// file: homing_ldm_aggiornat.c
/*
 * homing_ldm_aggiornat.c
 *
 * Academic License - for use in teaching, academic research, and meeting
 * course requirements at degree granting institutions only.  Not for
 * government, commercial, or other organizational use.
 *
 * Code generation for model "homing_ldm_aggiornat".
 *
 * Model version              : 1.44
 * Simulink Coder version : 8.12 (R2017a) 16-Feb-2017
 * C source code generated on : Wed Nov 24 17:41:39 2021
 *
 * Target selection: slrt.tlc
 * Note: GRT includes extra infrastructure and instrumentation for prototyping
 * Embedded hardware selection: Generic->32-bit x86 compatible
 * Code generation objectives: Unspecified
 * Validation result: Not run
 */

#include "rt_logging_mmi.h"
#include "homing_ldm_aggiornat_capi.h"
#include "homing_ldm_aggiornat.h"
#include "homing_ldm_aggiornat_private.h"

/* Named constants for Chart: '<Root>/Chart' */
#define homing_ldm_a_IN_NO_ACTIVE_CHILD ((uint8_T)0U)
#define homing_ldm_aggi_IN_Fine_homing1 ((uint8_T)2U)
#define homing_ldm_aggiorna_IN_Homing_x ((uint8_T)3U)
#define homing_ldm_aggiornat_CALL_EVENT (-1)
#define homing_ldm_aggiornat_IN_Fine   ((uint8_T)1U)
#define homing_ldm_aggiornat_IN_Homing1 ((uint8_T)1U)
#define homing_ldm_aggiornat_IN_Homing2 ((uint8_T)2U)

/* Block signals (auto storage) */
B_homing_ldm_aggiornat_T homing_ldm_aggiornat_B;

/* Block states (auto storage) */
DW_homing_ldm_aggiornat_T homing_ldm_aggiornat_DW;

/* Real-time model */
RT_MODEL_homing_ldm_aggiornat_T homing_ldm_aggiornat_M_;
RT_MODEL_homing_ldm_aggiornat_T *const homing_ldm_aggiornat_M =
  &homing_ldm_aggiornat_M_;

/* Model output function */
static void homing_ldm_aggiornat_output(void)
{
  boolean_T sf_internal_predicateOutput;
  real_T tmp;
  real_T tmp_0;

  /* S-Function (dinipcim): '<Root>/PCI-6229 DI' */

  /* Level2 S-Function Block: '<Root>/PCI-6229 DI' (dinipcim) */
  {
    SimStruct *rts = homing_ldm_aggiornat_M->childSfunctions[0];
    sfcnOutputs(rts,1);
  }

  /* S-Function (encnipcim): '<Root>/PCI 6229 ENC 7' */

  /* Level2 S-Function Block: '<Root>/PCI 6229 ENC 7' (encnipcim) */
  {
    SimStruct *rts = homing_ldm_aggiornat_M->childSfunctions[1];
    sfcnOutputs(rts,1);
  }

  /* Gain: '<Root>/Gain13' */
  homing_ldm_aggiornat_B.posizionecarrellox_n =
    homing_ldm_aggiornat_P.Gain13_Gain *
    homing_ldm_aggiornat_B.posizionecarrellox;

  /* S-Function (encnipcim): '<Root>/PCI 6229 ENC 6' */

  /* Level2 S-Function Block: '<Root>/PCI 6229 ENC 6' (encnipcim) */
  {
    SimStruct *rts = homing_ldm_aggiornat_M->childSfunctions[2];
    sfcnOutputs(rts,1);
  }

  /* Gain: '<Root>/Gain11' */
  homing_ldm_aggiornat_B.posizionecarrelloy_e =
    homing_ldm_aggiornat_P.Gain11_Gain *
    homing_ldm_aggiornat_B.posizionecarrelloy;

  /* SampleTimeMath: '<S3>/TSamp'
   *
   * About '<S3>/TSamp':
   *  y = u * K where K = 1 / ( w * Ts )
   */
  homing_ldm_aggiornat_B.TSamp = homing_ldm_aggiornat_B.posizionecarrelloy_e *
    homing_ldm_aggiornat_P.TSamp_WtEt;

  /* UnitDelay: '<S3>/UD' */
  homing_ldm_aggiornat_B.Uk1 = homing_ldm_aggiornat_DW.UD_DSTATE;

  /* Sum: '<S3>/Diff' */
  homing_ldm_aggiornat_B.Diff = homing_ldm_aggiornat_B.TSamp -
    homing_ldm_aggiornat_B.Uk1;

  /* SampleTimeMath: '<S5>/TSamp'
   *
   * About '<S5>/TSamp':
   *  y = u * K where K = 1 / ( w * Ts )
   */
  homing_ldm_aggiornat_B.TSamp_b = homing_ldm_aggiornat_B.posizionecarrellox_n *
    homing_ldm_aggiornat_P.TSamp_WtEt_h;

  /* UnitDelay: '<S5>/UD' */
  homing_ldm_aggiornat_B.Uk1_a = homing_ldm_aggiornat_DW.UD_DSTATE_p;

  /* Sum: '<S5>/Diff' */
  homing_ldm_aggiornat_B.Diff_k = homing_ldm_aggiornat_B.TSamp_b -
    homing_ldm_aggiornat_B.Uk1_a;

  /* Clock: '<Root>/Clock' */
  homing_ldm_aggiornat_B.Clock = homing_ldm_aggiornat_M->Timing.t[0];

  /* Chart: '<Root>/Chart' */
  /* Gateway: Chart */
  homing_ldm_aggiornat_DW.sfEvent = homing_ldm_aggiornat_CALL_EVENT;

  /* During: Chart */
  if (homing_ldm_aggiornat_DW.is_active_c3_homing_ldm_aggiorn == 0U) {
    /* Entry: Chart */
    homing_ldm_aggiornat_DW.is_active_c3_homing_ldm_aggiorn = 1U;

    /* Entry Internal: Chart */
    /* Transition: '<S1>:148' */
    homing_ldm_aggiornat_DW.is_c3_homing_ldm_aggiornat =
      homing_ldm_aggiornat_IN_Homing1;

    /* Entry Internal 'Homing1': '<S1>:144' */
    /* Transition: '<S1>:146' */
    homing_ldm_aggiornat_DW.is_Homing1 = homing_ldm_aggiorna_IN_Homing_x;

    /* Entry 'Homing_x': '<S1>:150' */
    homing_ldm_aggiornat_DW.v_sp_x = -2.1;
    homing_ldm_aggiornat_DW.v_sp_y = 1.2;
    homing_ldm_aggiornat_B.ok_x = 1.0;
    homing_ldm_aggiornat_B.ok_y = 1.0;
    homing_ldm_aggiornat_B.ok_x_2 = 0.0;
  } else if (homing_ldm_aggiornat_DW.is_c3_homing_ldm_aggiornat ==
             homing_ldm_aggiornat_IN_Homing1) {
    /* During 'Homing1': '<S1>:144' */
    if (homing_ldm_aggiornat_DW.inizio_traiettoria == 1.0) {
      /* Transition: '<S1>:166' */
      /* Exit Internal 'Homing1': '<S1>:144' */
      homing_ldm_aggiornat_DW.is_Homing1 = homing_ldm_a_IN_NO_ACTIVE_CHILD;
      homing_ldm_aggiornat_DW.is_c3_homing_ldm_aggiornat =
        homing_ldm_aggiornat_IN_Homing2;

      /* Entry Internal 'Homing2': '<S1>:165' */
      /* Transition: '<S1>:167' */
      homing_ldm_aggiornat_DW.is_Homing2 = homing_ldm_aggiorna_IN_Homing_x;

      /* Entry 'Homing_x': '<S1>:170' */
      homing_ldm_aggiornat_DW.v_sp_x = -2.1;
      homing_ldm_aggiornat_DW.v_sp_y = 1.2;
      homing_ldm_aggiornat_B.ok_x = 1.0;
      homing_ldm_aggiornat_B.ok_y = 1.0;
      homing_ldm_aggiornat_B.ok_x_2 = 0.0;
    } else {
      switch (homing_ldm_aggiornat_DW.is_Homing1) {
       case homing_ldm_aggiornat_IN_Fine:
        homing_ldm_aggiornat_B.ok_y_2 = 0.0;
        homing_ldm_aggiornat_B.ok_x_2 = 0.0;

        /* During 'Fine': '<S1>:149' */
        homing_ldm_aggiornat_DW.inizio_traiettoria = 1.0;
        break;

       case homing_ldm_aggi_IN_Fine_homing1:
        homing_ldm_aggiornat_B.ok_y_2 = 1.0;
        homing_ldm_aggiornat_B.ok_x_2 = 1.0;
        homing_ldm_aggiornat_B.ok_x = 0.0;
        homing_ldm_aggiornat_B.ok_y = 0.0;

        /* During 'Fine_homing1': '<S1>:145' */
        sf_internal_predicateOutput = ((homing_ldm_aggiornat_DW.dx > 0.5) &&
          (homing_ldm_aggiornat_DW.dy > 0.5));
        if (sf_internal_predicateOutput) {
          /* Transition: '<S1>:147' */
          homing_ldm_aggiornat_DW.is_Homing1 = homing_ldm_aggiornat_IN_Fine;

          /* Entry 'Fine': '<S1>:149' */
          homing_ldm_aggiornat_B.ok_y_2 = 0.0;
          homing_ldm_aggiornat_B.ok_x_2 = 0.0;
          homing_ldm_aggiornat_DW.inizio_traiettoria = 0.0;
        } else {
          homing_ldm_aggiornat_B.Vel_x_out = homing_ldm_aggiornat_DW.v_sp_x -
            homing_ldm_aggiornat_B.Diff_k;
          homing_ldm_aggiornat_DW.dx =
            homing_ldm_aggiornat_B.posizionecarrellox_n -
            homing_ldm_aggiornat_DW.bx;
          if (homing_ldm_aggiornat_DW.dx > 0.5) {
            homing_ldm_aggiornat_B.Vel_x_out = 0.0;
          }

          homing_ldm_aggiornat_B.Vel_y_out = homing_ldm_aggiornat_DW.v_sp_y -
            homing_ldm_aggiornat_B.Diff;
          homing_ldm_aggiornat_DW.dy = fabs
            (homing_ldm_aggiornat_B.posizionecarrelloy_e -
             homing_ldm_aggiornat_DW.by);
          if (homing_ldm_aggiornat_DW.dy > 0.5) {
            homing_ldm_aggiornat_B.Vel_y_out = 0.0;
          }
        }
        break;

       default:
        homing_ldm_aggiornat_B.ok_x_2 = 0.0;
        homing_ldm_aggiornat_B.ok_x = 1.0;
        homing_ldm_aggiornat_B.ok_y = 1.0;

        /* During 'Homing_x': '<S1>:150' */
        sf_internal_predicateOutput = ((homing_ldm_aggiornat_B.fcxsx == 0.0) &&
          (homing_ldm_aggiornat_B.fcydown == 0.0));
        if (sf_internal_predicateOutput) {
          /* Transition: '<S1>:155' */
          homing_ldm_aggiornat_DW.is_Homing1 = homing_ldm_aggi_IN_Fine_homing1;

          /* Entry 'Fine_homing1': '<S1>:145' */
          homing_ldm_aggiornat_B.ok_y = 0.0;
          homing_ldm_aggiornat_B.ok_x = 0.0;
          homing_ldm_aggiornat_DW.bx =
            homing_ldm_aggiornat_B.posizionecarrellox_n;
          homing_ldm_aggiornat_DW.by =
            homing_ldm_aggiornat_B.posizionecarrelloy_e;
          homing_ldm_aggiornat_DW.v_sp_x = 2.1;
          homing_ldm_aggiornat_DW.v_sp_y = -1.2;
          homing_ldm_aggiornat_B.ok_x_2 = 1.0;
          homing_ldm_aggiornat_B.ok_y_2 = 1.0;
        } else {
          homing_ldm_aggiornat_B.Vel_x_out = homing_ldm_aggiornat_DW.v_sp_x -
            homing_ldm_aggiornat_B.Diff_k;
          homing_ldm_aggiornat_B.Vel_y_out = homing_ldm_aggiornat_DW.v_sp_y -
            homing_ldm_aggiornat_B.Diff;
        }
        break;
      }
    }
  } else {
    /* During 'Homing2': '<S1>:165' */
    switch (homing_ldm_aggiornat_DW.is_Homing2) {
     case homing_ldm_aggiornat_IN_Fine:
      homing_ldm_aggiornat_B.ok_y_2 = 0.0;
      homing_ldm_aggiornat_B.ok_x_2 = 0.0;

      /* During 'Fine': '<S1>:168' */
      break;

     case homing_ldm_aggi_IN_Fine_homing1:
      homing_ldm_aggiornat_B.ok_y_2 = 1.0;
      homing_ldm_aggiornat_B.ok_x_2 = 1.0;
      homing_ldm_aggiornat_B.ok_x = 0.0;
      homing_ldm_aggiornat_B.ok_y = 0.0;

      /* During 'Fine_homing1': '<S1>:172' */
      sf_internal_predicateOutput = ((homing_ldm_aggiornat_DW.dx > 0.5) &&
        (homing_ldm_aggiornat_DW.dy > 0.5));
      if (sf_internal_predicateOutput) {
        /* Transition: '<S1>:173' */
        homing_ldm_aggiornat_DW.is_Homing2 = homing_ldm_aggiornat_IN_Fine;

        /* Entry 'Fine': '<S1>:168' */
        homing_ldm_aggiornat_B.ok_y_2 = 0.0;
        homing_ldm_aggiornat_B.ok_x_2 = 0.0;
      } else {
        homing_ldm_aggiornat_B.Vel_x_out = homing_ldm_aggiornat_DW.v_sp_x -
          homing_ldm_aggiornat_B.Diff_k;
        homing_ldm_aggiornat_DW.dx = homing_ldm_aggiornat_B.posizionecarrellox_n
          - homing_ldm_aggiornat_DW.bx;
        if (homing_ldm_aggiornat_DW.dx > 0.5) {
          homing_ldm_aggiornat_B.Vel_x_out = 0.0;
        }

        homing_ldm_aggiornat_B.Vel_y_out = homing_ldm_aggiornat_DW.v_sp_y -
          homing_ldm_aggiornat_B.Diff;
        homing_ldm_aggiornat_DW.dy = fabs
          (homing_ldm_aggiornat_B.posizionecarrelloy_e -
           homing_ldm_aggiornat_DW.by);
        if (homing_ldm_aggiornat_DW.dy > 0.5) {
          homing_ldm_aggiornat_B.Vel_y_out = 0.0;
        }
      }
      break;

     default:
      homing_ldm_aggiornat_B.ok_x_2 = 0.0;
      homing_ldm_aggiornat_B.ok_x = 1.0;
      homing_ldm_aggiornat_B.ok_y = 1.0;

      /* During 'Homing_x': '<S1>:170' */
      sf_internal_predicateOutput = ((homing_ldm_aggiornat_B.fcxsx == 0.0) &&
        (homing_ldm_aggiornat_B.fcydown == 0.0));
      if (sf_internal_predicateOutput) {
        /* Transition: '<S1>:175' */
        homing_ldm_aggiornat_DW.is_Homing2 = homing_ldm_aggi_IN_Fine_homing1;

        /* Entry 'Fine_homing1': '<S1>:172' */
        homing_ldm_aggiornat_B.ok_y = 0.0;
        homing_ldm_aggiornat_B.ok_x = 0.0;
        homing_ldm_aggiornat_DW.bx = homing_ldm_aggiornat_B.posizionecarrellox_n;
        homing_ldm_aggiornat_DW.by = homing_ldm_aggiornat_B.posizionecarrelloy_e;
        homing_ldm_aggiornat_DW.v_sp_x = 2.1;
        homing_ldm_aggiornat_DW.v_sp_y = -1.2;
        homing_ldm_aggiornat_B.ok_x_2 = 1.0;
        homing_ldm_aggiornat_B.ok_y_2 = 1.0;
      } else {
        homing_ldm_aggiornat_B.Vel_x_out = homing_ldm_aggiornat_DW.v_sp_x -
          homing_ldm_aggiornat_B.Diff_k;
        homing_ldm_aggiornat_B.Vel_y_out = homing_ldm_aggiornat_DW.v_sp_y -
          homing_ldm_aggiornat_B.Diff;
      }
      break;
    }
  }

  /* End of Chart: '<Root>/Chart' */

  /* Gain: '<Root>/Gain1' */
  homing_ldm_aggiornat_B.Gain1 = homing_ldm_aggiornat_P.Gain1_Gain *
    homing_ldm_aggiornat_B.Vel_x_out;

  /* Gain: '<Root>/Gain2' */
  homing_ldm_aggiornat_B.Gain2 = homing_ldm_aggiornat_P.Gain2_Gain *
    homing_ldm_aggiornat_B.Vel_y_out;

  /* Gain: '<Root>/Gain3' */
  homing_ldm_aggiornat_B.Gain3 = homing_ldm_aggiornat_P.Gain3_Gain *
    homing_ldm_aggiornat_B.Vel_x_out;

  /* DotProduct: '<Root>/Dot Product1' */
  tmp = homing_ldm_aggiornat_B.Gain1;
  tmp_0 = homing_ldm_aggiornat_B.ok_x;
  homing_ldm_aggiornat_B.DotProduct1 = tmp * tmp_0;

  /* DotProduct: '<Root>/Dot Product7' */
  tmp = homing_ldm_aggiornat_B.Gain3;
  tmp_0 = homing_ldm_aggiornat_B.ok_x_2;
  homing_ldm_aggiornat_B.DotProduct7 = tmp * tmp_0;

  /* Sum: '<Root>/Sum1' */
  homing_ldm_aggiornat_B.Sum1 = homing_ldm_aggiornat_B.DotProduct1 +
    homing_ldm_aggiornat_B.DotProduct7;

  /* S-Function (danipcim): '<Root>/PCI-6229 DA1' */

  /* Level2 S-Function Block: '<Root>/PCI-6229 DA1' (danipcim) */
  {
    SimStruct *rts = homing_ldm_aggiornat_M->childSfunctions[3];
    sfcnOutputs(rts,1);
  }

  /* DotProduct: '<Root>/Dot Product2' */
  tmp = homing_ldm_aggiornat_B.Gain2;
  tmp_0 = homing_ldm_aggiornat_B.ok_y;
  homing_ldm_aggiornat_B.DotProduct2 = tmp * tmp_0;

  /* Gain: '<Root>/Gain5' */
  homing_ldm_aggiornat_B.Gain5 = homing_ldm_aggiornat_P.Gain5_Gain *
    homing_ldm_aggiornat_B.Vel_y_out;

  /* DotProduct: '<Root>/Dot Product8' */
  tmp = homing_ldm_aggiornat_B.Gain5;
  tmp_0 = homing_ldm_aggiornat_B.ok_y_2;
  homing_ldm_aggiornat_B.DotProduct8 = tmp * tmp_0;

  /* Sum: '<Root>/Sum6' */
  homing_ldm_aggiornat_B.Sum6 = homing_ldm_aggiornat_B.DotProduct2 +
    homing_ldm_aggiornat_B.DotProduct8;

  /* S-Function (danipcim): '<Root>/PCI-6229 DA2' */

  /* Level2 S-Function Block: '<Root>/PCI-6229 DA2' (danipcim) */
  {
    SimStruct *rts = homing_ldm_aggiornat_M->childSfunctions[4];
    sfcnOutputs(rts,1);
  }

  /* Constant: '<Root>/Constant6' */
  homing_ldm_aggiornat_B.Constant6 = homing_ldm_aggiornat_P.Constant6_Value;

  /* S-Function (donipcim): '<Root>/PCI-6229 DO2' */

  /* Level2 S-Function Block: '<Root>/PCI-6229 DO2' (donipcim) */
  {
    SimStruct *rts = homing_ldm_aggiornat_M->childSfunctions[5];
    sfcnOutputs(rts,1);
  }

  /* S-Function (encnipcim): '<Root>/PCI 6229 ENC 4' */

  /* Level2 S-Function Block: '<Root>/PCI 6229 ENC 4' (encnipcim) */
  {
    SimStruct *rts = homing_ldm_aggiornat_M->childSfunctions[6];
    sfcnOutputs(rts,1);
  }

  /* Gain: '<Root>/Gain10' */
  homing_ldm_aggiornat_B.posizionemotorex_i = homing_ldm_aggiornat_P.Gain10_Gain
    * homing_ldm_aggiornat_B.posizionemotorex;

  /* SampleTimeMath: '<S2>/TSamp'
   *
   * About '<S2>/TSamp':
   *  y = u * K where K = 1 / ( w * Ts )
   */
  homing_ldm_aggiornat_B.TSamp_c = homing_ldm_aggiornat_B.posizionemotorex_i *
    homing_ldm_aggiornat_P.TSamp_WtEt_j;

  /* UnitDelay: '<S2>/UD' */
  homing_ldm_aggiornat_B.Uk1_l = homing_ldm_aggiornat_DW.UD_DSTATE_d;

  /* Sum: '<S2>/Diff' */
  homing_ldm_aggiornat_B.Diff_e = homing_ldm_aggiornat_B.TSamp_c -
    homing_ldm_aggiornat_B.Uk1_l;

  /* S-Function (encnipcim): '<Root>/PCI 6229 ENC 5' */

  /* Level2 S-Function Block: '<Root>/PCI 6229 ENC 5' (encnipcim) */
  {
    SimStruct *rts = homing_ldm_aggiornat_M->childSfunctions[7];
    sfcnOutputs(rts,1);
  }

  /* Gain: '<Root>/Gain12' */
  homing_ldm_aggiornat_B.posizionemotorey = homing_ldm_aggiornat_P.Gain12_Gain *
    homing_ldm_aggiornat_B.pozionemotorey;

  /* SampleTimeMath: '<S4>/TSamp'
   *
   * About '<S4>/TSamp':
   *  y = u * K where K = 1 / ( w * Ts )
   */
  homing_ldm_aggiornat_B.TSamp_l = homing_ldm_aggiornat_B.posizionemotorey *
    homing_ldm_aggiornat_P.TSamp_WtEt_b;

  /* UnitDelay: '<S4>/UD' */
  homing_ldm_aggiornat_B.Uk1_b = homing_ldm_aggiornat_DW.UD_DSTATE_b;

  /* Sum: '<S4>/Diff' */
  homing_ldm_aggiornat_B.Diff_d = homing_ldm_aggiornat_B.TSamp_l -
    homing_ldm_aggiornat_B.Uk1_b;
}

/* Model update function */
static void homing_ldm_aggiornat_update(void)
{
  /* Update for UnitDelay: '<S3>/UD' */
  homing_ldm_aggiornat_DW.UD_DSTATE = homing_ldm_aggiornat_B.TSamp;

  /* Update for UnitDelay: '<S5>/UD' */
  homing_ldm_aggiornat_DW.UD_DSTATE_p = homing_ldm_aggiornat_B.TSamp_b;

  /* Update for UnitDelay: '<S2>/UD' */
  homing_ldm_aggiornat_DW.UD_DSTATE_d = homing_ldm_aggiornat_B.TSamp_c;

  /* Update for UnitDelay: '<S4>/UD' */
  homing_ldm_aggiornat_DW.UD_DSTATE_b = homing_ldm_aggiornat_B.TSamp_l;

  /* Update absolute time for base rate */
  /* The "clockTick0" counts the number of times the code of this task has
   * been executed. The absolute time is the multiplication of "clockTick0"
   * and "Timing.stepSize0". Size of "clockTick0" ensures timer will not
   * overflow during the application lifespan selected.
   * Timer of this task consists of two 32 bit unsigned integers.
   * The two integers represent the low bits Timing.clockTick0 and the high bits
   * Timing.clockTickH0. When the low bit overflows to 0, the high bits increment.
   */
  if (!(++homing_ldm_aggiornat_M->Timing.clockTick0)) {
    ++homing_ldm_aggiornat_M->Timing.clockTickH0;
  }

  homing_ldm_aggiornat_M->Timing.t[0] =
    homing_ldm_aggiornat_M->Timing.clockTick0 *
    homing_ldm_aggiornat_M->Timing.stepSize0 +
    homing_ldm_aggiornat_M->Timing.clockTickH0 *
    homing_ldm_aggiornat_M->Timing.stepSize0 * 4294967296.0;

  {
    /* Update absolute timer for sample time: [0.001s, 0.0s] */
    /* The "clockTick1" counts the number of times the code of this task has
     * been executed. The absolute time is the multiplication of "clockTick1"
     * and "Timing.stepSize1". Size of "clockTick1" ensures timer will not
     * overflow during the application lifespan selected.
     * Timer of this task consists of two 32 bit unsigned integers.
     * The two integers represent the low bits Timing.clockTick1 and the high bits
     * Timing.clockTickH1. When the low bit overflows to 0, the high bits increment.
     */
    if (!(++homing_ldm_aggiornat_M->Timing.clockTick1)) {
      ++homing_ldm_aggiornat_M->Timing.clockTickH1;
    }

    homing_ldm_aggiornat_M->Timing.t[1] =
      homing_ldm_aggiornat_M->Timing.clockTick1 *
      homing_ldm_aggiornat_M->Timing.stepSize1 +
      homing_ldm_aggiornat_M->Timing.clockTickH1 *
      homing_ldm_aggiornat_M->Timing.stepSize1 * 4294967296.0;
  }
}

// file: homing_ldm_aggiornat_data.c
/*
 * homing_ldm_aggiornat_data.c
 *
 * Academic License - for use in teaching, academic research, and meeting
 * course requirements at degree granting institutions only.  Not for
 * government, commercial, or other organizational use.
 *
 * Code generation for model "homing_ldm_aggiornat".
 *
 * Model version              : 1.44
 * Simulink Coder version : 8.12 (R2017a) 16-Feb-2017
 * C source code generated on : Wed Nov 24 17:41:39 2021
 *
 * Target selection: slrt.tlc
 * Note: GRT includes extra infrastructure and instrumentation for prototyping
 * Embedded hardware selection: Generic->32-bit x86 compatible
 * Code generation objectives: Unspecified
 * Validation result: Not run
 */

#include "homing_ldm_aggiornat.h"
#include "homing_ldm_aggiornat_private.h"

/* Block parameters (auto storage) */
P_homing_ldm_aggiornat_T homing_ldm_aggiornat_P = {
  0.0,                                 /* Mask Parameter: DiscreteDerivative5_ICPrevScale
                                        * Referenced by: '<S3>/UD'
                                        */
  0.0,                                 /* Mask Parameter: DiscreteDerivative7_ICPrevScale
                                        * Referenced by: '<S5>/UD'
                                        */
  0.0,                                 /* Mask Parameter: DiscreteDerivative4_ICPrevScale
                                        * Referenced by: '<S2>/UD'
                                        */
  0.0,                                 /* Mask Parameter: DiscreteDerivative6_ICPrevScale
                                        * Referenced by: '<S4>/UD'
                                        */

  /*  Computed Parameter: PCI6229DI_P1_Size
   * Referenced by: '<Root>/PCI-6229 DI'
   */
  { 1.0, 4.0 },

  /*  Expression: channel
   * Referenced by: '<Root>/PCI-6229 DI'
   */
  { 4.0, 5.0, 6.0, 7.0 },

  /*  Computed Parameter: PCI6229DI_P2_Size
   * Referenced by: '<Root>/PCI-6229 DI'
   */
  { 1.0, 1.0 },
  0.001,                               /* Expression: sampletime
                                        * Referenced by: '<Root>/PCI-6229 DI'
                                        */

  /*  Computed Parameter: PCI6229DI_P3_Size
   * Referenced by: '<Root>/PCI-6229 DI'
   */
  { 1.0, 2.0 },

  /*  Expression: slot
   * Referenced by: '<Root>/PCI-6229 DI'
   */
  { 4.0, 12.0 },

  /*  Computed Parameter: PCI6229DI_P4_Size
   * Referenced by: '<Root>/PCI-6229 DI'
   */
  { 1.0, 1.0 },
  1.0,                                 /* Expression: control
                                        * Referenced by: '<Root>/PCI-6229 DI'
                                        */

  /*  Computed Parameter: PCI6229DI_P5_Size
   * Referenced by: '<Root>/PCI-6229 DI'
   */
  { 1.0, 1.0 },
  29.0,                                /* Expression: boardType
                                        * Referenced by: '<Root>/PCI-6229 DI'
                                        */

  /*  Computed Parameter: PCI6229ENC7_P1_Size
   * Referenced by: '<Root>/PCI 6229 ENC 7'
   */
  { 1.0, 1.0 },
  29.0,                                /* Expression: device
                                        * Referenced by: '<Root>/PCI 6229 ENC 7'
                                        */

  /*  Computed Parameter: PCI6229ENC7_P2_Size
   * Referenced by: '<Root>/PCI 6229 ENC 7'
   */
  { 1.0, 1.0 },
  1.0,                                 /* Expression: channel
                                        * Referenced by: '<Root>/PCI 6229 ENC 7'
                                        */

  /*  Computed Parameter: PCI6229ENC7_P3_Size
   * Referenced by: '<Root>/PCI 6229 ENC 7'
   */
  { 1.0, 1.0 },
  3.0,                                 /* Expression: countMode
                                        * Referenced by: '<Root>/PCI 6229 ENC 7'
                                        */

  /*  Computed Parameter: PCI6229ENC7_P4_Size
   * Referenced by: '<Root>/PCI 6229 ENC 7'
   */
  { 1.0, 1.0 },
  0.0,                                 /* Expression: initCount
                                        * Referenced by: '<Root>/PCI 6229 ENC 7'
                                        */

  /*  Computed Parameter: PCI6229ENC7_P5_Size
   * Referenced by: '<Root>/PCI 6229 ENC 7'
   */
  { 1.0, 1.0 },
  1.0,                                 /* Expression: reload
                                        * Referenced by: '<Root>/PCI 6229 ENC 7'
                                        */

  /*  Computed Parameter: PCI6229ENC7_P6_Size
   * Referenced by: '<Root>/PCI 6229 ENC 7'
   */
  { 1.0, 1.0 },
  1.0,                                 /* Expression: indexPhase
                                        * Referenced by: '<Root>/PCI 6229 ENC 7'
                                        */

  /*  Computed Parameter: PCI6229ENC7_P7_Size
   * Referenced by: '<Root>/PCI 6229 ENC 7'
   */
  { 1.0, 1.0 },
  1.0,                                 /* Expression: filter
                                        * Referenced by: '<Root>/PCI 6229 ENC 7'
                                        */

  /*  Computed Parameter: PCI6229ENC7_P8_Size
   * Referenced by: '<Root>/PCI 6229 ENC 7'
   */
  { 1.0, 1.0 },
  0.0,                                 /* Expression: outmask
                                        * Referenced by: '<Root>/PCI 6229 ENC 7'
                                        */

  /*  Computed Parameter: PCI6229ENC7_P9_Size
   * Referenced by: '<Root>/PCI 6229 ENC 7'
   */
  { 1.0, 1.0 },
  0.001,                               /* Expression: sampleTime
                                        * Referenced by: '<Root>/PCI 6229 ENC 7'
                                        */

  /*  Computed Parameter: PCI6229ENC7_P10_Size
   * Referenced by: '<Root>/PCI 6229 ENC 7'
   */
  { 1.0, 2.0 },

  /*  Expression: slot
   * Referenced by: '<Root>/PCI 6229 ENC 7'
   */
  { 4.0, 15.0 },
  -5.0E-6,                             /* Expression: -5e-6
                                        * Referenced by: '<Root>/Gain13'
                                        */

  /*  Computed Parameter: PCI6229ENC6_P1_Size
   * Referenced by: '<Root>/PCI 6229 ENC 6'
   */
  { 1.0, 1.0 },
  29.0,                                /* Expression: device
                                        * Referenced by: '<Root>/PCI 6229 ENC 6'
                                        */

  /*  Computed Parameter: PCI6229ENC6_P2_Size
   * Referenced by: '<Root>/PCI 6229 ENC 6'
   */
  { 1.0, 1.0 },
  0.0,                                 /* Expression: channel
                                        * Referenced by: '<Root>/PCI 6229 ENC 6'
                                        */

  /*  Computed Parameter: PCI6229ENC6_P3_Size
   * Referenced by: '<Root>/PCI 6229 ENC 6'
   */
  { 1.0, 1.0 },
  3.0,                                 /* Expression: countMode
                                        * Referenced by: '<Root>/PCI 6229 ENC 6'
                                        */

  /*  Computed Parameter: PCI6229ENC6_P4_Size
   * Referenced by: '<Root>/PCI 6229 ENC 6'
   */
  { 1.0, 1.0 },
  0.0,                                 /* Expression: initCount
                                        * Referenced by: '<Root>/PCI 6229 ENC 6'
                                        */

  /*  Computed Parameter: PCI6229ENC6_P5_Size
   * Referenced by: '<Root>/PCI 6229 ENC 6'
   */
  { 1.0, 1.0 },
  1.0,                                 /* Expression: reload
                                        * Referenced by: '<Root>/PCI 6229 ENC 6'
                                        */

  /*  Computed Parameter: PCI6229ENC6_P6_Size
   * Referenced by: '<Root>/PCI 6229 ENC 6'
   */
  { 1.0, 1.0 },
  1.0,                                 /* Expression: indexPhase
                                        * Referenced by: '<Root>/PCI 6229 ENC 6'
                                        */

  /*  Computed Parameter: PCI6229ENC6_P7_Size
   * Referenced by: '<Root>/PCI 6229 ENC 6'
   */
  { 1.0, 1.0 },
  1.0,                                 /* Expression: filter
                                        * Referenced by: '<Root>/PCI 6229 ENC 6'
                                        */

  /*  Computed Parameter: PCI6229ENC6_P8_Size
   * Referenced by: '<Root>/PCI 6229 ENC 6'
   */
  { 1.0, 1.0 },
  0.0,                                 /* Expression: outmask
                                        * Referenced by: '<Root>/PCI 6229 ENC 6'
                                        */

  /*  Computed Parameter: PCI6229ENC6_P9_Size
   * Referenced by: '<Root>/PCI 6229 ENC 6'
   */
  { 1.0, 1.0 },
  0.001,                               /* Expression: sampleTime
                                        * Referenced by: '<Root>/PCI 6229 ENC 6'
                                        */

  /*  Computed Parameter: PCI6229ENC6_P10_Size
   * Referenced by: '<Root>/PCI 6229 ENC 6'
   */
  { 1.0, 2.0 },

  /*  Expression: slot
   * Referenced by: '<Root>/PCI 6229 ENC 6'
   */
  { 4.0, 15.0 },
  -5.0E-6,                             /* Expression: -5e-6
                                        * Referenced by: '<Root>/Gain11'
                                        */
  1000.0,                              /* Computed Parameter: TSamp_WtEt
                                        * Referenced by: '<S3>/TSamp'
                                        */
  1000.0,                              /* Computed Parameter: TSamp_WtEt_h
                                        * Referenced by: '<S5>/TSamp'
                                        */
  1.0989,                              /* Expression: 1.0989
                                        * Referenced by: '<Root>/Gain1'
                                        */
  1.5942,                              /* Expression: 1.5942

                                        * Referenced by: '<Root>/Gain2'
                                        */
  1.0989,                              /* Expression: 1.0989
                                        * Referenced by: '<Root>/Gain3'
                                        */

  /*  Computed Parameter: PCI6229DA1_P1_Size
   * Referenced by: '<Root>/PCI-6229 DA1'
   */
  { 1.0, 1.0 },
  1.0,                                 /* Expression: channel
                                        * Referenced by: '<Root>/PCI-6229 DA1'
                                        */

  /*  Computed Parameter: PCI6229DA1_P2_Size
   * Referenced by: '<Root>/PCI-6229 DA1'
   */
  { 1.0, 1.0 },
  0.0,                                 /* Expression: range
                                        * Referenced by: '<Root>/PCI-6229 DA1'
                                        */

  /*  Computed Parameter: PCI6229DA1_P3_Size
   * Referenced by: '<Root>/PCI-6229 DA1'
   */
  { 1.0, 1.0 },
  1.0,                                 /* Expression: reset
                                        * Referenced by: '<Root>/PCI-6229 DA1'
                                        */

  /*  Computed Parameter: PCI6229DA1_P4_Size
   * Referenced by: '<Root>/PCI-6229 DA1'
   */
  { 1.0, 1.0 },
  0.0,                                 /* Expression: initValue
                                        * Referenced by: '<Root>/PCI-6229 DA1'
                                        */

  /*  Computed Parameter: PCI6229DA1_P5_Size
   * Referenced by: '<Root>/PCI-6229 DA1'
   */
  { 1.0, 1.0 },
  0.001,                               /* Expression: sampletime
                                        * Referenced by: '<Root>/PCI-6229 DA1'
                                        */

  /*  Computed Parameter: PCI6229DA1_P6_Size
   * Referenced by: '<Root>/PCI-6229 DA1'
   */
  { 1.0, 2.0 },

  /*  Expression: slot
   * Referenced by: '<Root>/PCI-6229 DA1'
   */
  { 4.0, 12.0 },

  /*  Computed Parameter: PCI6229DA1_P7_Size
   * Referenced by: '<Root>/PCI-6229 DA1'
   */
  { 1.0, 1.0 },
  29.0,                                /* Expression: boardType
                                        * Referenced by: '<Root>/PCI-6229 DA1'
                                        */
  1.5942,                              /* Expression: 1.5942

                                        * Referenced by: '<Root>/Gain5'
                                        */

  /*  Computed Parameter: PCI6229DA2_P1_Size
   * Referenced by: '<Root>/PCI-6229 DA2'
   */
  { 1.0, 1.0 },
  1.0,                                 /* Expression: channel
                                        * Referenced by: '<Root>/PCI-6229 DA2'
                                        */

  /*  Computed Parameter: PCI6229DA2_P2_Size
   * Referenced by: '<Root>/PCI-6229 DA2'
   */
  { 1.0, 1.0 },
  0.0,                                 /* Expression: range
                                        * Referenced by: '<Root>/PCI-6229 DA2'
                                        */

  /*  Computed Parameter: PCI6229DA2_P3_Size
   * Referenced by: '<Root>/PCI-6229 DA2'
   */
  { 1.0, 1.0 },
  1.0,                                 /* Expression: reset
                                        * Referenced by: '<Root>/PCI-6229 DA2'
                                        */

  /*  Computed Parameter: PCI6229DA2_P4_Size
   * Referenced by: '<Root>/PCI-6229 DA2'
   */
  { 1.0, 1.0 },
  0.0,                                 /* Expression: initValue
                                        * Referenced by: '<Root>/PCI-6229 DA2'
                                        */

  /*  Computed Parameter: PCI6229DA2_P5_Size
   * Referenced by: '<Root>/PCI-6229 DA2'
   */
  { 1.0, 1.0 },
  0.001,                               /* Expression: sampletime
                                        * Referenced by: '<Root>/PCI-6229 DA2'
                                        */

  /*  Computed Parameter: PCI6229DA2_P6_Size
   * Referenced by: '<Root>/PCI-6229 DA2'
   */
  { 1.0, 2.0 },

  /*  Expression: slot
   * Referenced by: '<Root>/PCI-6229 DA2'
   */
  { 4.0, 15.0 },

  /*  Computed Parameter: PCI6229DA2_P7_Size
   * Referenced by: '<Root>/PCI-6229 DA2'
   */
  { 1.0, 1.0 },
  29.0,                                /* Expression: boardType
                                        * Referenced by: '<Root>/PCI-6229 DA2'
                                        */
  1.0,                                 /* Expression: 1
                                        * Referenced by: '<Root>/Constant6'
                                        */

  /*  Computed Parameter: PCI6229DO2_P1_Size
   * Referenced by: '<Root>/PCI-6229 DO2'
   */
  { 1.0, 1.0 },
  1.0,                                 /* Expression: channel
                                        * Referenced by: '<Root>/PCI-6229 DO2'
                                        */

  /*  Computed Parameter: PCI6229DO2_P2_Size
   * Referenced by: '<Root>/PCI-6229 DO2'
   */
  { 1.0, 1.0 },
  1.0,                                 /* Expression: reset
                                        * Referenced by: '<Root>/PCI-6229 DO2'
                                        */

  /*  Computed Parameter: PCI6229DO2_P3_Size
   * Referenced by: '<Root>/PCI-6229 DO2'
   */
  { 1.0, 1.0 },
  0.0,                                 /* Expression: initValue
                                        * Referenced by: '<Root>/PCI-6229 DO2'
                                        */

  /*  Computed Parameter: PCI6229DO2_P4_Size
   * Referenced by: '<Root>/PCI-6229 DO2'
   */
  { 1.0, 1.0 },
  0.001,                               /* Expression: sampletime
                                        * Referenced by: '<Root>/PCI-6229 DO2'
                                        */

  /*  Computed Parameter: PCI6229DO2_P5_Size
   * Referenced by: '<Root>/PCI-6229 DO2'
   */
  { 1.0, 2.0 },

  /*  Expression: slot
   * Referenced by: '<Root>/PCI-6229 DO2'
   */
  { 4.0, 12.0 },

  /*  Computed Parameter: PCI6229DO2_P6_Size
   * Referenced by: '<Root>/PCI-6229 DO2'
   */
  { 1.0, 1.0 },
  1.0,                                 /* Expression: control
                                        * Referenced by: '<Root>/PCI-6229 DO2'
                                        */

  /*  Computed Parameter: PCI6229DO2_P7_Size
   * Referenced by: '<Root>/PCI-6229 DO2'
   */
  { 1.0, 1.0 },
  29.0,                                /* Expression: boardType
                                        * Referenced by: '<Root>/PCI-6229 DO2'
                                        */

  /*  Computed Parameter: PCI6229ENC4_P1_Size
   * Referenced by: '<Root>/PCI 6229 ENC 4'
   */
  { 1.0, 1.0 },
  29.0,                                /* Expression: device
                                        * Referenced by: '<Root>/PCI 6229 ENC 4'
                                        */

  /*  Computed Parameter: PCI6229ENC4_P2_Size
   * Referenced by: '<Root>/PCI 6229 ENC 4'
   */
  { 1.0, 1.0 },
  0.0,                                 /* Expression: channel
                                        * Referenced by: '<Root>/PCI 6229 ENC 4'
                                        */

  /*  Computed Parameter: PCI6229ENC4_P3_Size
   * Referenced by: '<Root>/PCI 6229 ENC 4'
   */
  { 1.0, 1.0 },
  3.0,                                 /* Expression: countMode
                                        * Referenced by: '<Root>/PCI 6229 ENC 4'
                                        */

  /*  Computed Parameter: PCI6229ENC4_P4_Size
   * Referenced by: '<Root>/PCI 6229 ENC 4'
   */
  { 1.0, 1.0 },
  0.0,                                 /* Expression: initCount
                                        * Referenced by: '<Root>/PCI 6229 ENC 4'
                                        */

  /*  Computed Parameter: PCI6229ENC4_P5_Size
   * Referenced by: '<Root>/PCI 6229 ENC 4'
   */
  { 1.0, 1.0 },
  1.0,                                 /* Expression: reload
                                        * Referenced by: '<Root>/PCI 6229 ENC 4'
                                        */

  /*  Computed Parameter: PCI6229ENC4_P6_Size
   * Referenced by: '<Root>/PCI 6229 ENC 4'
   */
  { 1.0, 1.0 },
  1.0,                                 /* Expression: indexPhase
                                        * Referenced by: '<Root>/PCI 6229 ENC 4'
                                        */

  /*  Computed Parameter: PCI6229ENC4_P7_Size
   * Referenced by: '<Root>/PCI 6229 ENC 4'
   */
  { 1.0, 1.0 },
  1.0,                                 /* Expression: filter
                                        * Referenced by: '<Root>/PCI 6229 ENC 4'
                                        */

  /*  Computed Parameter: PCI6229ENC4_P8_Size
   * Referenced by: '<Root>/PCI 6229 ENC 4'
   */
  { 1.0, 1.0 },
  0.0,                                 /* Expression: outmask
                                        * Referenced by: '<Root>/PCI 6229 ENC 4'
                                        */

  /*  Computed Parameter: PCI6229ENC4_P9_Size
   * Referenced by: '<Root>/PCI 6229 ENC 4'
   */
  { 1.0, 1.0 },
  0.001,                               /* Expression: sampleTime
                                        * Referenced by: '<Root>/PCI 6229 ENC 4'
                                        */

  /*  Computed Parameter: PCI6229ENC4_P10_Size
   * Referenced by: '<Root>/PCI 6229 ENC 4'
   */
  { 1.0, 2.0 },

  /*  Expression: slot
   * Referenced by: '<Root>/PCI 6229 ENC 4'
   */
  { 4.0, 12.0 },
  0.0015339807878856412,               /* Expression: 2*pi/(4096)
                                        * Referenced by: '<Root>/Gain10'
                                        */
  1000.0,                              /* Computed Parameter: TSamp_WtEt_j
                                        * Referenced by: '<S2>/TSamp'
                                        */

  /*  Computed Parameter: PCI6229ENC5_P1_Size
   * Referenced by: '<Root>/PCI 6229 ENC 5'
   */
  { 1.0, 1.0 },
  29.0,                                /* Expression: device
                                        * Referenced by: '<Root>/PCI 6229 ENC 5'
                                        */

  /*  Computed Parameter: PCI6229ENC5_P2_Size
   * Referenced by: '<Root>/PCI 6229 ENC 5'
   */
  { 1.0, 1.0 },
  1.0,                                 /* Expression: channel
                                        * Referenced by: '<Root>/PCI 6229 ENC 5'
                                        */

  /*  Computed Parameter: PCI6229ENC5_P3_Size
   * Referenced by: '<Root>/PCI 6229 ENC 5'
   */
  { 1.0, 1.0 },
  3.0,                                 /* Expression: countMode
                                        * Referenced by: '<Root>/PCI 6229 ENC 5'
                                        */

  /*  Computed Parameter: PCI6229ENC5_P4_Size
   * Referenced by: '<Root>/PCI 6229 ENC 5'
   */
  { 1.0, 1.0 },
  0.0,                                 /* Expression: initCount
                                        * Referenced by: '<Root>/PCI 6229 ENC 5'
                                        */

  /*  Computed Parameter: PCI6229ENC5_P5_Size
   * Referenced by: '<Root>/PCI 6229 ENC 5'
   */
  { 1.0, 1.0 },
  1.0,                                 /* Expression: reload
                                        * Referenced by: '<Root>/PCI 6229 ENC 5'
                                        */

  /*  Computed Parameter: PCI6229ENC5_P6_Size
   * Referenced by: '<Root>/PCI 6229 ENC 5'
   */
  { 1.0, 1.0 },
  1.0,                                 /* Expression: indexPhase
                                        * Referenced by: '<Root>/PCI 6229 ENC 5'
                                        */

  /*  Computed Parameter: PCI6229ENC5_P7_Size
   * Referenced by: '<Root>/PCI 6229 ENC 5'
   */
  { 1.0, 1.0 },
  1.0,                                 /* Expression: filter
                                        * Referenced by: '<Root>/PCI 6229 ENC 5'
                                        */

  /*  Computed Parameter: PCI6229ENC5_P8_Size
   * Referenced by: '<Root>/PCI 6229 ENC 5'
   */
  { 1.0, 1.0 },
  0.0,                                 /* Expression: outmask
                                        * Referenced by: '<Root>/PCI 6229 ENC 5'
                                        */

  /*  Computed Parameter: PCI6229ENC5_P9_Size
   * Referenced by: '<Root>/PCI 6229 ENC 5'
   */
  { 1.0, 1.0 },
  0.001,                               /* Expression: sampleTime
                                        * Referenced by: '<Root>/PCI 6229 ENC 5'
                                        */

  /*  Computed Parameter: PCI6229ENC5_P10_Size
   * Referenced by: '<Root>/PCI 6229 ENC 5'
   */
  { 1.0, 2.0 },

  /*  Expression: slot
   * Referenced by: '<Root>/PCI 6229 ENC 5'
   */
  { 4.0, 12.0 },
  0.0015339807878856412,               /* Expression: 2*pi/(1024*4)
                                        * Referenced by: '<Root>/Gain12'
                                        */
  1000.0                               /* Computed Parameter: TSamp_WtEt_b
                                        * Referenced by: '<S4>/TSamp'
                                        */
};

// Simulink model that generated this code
simulink model "homing_ldm_aggiornat"  (R2017a)
settings: Solver=FixedStepAuto  StartTime=0.0  StopTime=inf  FixedStep=1e-3  RelTol=1e-3  EnableMultiTasking=on
libraries: xpcnilib x10, simulink x4

== system homing_ldm_aggiornat ==
  note: Finecorsa
  note: Homing x
  note: Encoder Motore sull'asse y
      | Da qua prendo la misura di theta1
  note: encoder asse y
  note: encoder asse x
  note: Banda sull'asse y (CARRELLO)
  note: comando tensione motore x (positivo a dx)
  note: Encoder Motore sull'asse x
      | Da qua prendo la misura di theta1
  note: enable P0.0
  note: Banda sull'asse x (CARRELLO)
  note: Scarto velocità asse x
  note: Homing x
  note: homing y
  Chart : Stateflow chart  TreatAsAtomicUnit=on
  Clock : Clock
  Constant6 : Constant
  Constant7 : Constant  Commented=on  Value=-2
  Constant8 : Constant  Commented=on  Value=2
  Discrete Derivative{4..7} (4 alike) : simulink/Discrete/Discrete Derivative  gainval=1.0  ICPrevScaledInput=0.0  OutMin=[]  OutMax=[]  OutDataType=fixdt(1, 16)  OutScaling=2^-10  DoSatur=off
  Display{,1..3,7..8,10..11} (8 alike) : Display
  Dot Product{1..2,7..8} (4 alike) : DotProduct  InputSameDT=on  OutDataTypeStr=Inherit: Inherit via internal rule
  Gain1 : Gain  Gain=1.0989
  Gain10 : Gain  Gain=2*pi/(4096)
  Gain11 : Gain  Gain=-5e-6
  Gain12 : Gain  Gain=2*pi/(1024*4)
  Gain13 : Gain  Gain=-5e-6
  Gain2 : Gain  Gain=1.5942
  Gain3 : Gain  Gain=1.0989
  Gain5 : Gain  Gain=1.5942
  PCI 6229 ENC 4 : xpcnilib/Incremental Encoder/PCI 6229 ENC   channel=0  countMode=Quadrature Mode x4  initCount=0  reload=on  indexPhase=A low B low  filter=None  sampleTime=0.001  slot=[4 12]
  PCI 6229 ENC 5 : xpcnilib/Incremental Encoder/PCI 6229 ENC   channel=1  countMode=Quadrature Mode x4  initCount=0  reload=on  indexPhase=A low B low  filter=None  sampleTime=0.001  slot=[4 12]
  PCI 6229 ENC 6 : xpcnilib/Incremental Encoder/PCI 6229 ENC   channel=0  countMode=Quadrature Mode x4  initCount=0  reload=on  indexPhase=A low B low  filter=None  sampleTime=0.001  slot=[4 15]
  PCI 6229 ENC 7 : xpcnilib/Incremental Encoder/PCI 6229 ENC   channel=1  countMode=Quadrature Mode x4  initCount=0  reload=on  indexPhase=A low B low  filter=None  sampleTime=0.001  slot=[4 15]
  PCI-6229 DA1 : xpcnilib/D//A/M Series/PCI-6229 DA  channel=[1]  reset=[1]  initValue=[0]  sampletime=0.001  slot=[4 12]
  PCI-6229 DA2 : xpcnilib/D//A/M Series/PCI-6229 DA  channel=[1]  reset=[1]  initValue=[0]  sampletime=0.001  slot=[4 15]
  PCI-6229 DA6 : xpcnilib/D//A/M Series/PCI-6229 DA  Commented=on  channel=[1]  reset=[1]  initValue=[0]  sampletime=0.001  slot=[4 12]
  PCI-6229 DA7 : xpcnilib/D//A/M Series/PCI-6229 DA  Commented=on  channel=[1]  reset=[1]  initValue=[0]  sampletime=0.001  slot=[4 15]
  PCI-6229 DI : xpcnilib/Digital Input/M Series/PCI-6229 DI  channel=[4 5 6 7]  sampletime=0.001  slot=[4 12]
  PCI-6229 DO2 : xpcnilib/Digital Output/M Series/PCI-6229 DO  channel=[1]  reset=[1]  initValue=[0]  sampletime=0.001  slot=[4 12]
  Scope1 : Scope  NumInputPorts=2
  Scope3 : Scope  NumInputPorts=2
  Sum1 : Sum  Inputs=|++
  Sum6 : Sum  Inputs=|++
  Terminator : Terminator
  wires:
  PCI-6229 DI/1 -> [Fcx_sx], Display/1  "fc x sx"
  PCI-6229 DI/2 -> Display1/1  "fc x dx"
  PCI-6229 DI/3 -> Display2/1  "fc y high"
  PCI-6229 DI/4 -> [Fcy_dw], Display3/1  "fc y down"
  [Fcx_sx] -> Chart/1(fcx)
  [Vel_car_x] -> Chart/2(Vel_x)
  Chart/1(Vel_x_out) -> [dV_x]
  [Fcy_dw] -> Chart/4(fcy)
  [Vel_car_y] -> Chart/3(Vel_y)
  Chart/2(ok_x) -> [ok_x]
  Chart/3(ok_y) -> [ok_y]
  Chart/4(Vel_y_out) -> [dV_y]
  [Pos_car_x] -> Chart/5(Pos_x)
  Chart/5(ok_x_2) -> [ok_x_2]
  Chart/6(ok_y_2) -> [ok_y_2]
  [Pos_car_y] -> Chart/6(Pos_y)
  Clock/1 -> Chart/7(clock)
  ? -> Terminator/1  "X"
  Gain13/1 -> Discrete Derivative7/1, [Pos_car_x], Display10/1  "posizione carrello x"
  Constant6/1 -> PCI-6229 DO2/1
  Constant8/1 -> PCI-6229 DA6/1
  Discrete Derivative4/1 -> Scope1/2  "velocità motore x"
  Discrete Derivative6/1 -> Scope3/2  "velocità motore y"
  Constant7/1 -> PCI-6229 DA7/1
  PCI 6229 ENC 5/1 -> Gain12/1  "pozione motore y"
  Discrete Derivative7/1 -> [Vel_car_x]  "velocità carrello x"
  Gain11/1 -> [Pos_car_y], Display8/1, Discrete Derivative5/1  "posizione carrello y"
  Gain10/1 -> Display7/1, Scope1/1, Discrete Derivative4/1  "posizione motore x"
  Discrete Derivative5/1 -> [Vel_car_y]  "velocità carrello y"
  PCI 6229 ENC 4/1 -> Gain10/1  "posizione motore x"
  PCI 6229 ENC 6/1 -> Gain11/1  "posizione carrello y"
  PCI 6229 ENC 7/1 -> Gain13/1  "posizione carrello x"
  Gain12/1 -> Scope3/1, Display11/1, Discrete Derivative6/1  "posizione motore y"
  Dot Product2/1 -> Sum6/1
  [dV_y] -> Gain5/1
  Gain3/1 -> Dot Product7/1
  Dot Product8/1 -> Sum6/2
  Sum6/1 -> PCI-6229 DA2/1
  Sum1/1 -> PCI-6229 DA1/1
  Dot Product1/1 -> Sum1/1
  Gain5/1 -> Dot Product8/1
  Gain2/1 -> Dot Product2/1
  [ok_y_2] -> Dot Product8/2
  [ok_x_2] -> Dot Product7/2
  [dV_x] -> Gain3/1
  [ok_x] -> Dot Product1/2
  Dot Product7/1 -> Sum1/2
  Gain1/1 -> Dot Product1/1
  [dV_y] -> Gain2/1
  [dV_x] -> Gain1/1
  [ok_y] -> Dot Product2/2

== stateflow chart homing_ldm_aggiornat/Chart ==
  state Homing1
    state Homing_x
      entry:
      v_sp_x=-2.1;
      v_sp_y=1.2;
      ok_x=1;
      ok_y=1;
      ok_x_2=0;
      during:
      Vel_x_out = v_sp_x-Vel_x;
      Vel_y_out=v_sp_y-Vel_y;
    note: Inizializzazione asse x
        | Inizializzazione asse y
    state Fine_homing1
      entry:
      ok_y=0;
      ok_x=0;
      bx=Pos_x;
      by=Pos_y;
      v_sp_x=2.1;
      v_sp_y=-1.2;
      ok_x_2=1;
      ok_y_2=1;
      during:
      Vel_x_out=v_sp_x-Vel_x;
      dx=Pos_x-bx
      if (dx>0.5 )
      Vel_x_out=0;
      end
      Vel_y_out=v_sp_y-Vel_y;
      dy=abs(Pos_y-by);
      if (dy>0.5 )
      Vel_y_out=0;
      end
    note: Fine inizializzazione
    note: Porto al centro asse x
        | Porto al centro asse y
    state Fine
      entry:
      ok_y_2=0;
      ok_x_2=0;
      inizio_traiettoria=0;
      during:
      inizio_traiettoria=1;
    (default) -> Homing_x
    Homing_x -> Homing1.Fine_homing1 : [fcx==0 && fcy==0]
    Homing1.Fine_homing1 -> Homing1.Fine : [dx>0.5 && dy>0.5]
  state Homing
    state Fine_homing1
      entry:
      ok_y=0;
      ok_x=0;
      a=Pos_x;
      ok_x_2=1;
      t1=clock;
      %X=0;
      %G_=0;
      %F_=0;
      %f_=0;
      during:
      t=clock-t1;
      %[G_,F_,f_]=Constant_Acceleration_ADIM_par(t,[1/3,1/3,1/3]);
      X_=Evaluate_Trajectory(t);
      Vel_x_out=X_;
      dx=Pos_x-a
    state Posizionamento_y
      entry:
      ok_x_2=0;
      ay=Pos_y;
      v_sp_y=-1.3;
      ok_y_2=1;
      during:
      Vel_y_out=v_sp_y-Vel_y;
      dy=abs(Pos_y-ay);
    state Fine
      entry:
      ok_y_2=0;
      ok_x_2=0;
    (default) -> Homing.Fine_homing1 : [fcy==0]
    Homing.Fine_homing1 -> Posizionamento_y : [dx>0.5]
    Posizionamento_y -> Homing.Fine : [dy>0.5]
  (default) -> Homing1
  Homing1.Fine -> Homing : [inizio_traiettoria==1]
  data: t1 local double; t local double; t function_input; X function_output; fcx input; Vel_x_out output; Vel_x input; ok_x output; ok_y output; Vel_y input; Vel_y_out output; fcy input; Pos_x input; dx local; ok_x_2 output; v_sp_x local; a local; v_sp_y local; ay local; Pos_y input; ok_y_2 output; dy local; clock input; bx local; by local; inizio_traiettoria local
  function X=Evaluate_Trajectory(t):
    | function X=Evaluate_Trajectory(t)
    | % parametri:
    | % t: tempo assolu
    | % h: spostamento richiesto
    | y=0;
    | yp=0;
    | ypp=0;
    | X=0;
    | 
    | h=0.5;
    | h0=0;
    | DT=[1/5 1/3 1/3 0]; %ta di ogni singolo ramo perche' composta
    | 
    | par = [1/3, 2/3];
    | 
    | 
    | DT1 = DT(1);
    | DT2 = DT(2);
    | DT3 = DT(3);
    | DT4 = DT(4);
    | 
    | T0 = 0;
    | T1 = T0 + DT1;
    | T2 = T1 + DT2;
    | T3 = T2 + DT3;
    | T4  = T3 + DT4;                  % Total time
    | 
    | if t >= T0 && t <= T1            % Interval N°1 
    |    td = DT1; %tempo di azionamento
    |    x = (t - T0)/td; %tempo adimensionale
    |    
    |    [G,F,f] = Constant_Acceleration_ADIM_par(x,par);
    |    y = h0 + G*h;
    |    yp = F * h/td;
    |    ypp = f * h/td^2;
    | end
    | 
    | if t > T1 && t <= T2             % Interval N°2 
    |    y = h0 + h;
    |    yp = 0;
    |    ypp = 0;
    | end
    | 
    | if t > T2 && t <= T3             % Interval N°3
    |    td = DT3;
    |    x = (t - T2)/td;
    |    
    |    [G,F,f] = Constant_Acceleration_ADIM_par(x,par);
    | 
    |    y = (h0 + h) - G*h;
    |    yp =  - (F * h/td);
    |    ypp = - (f * h/td^2);
    | end
    | 
    | if t > T3               % Interval N°4    
    |    y = h0;
    |    yp = 0;
    |    ypp = 0;  
    | end
    | Y = [y,yp,ypp];
    | X=yp;%pos, vel, acc
